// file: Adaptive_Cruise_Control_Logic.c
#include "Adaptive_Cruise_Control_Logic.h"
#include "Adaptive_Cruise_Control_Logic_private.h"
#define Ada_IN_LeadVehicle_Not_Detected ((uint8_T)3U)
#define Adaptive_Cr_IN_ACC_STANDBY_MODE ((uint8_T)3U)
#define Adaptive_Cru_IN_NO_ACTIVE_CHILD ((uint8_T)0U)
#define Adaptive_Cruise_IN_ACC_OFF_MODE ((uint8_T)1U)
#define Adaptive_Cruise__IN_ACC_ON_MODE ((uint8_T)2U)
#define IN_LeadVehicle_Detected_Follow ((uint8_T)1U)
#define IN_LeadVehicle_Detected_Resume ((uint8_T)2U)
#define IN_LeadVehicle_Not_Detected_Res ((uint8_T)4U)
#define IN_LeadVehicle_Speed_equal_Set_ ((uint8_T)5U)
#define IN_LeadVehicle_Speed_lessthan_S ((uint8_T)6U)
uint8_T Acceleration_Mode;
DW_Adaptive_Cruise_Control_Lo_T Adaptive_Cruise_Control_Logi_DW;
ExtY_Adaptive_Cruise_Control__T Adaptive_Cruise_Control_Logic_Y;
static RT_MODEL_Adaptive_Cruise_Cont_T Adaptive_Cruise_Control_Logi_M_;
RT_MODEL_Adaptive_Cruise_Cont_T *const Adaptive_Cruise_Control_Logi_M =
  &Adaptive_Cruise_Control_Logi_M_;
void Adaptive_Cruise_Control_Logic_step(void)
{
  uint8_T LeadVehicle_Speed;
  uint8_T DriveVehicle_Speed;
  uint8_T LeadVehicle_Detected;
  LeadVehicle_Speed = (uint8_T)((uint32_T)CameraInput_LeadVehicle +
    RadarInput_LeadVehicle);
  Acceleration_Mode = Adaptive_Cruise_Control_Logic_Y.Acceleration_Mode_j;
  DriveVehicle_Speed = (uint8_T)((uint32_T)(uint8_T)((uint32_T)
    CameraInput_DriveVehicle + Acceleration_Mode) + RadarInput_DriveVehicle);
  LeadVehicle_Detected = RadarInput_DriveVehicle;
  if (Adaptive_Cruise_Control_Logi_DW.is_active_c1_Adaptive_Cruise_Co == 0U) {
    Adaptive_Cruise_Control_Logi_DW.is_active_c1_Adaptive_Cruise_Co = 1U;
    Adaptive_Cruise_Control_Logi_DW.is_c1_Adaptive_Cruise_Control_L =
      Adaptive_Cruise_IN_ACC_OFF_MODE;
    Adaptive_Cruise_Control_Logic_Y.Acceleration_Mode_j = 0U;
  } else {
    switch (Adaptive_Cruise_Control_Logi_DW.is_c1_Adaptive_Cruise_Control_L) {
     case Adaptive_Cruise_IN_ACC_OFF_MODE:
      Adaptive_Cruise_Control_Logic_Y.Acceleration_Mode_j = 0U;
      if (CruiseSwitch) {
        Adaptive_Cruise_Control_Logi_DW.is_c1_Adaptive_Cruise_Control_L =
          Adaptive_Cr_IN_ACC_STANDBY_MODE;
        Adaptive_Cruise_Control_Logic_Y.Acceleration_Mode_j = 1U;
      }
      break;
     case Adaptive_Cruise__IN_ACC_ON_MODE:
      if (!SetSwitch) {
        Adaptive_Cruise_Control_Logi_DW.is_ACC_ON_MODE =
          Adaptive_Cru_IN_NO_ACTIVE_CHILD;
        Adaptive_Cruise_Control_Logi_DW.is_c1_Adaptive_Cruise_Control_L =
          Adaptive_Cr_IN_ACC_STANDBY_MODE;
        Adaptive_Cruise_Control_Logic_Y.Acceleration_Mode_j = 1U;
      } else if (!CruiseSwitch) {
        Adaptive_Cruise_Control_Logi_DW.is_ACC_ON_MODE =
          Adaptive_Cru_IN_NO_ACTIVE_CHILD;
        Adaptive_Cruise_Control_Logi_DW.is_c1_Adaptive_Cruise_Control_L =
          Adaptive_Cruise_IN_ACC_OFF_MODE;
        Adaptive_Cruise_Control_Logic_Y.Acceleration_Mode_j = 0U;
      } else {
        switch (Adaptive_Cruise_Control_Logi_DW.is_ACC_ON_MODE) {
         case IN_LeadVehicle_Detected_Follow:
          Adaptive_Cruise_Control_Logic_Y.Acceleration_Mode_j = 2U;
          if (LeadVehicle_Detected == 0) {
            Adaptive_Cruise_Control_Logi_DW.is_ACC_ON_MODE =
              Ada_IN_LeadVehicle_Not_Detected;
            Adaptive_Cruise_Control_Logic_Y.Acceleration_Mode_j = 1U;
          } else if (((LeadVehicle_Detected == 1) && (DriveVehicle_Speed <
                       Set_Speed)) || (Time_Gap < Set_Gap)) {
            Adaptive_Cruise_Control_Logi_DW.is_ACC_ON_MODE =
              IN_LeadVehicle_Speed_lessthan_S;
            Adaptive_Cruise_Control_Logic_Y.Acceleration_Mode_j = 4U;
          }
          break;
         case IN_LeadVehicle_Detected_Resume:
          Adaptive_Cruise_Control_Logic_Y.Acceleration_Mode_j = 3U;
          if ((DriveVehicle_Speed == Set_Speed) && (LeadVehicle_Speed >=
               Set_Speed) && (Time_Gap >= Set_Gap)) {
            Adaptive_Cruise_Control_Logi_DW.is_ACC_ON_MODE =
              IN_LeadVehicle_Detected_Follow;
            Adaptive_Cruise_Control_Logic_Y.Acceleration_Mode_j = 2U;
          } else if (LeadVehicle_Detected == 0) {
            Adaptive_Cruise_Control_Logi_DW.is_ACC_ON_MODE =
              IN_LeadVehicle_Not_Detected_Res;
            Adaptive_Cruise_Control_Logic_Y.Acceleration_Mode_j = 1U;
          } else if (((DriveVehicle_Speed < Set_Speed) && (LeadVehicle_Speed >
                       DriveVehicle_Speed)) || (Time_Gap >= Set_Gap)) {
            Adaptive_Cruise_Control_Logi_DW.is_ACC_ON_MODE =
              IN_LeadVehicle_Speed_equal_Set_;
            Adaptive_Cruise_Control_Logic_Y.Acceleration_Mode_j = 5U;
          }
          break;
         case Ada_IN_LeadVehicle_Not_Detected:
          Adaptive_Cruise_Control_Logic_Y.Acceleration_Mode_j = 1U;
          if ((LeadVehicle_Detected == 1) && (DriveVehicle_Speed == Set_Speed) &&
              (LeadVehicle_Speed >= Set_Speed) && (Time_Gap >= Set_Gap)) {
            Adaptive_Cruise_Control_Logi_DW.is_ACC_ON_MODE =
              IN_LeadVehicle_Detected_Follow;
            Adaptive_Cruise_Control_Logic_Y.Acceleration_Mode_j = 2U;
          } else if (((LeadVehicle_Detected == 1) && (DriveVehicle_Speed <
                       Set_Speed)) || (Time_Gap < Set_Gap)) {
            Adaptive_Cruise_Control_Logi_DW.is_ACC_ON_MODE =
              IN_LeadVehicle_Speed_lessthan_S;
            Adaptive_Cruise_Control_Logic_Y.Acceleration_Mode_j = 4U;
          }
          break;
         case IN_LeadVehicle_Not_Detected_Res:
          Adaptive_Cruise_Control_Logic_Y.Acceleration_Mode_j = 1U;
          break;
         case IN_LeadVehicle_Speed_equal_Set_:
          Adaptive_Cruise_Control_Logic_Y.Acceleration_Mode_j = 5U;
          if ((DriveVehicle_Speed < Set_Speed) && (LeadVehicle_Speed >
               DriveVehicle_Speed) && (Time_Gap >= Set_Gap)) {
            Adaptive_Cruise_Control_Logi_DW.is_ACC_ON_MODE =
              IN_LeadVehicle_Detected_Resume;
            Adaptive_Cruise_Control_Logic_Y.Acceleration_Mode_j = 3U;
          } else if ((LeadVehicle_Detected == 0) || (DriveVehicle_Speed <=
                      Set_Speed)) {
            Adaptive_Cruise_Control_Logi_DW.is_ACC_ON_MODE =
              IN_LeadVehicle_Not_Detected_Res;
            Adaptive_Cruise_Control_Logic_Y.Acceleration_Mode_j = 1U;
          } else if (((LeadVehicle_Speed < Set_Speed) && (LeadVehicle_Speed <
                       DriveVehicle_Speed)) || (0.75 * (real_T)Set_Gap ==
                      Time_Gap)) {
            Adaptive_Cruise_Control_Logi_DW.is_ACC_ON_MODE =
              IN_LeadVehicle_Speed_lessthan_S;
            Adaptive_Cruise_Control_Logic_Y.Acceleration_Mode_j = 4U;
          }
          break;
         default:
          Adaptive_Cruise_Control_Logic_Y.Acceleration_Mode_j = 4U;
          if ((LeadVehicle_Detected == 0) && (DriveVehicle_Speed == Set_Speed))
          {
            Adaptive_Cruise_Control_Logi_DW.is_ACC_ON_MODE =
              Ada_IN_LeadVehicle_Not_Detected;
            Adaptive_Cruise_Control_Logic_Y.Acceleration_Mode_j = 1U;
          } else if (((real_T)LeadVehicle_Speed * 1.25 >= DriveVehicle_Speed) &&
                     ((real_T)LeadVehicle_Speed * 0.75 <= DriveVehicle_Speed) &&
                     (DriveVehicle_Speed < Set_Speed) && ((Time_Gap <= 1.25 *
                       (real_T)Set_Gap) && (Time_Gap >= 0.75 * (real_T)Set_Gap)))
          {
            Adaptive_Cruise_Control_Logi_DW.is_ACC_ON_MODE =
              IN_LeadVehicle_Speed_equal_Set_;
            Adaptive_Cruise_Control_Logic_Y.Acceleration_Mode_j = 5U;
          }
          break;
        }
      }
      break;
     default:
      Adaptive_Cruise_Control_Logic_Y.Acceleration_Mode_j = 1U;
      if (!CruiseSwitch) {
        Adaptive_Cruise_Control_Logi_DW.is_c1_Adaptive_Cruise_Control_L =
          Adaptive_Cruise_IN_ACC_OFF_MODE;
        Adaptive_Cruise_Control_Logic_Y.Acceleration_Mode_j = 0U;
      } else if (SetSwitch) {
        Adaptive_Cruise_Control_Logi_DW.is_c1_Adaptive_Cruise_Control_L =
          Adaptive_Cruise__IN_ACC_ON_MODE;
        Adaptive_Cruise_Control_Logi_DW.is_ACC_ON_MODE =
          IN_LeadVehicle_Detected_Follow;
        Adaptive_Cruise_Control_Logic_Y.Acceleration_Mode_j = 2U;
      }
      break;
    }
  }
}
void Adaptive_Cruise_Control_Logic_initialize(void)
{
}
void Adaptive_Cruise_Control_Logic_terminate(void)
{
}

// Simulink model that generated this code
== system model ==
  CameraInput_LeadVehicle : Inport
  RadarInput_LeadVehicle : Inport
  CameraInput_DriveVehicle : Inport
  RadarInput_DriveVehicle : Inport
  CruiseSwitch : Inport
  Time_Gap : Inport
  Set_Speed : Inport
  Set_Gap : Inport
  SetSwitch : Inport
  Acceleration_Mode : Outport  <- 1: Subsystem#1
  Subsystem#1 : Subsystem  <- 1: CameraInput_LeadVehicle, 2: RadarInput_LeadVehicle, 3: CameraInput_DriveVehicle, 4: RadarInput_DriveVehicle, 5: CruiseSwitch, 6: Time_Gap, 7: Set_Speed, 8: Set_Gap, 9: SetSwitch
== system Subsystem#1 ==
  Inport#1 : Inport
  Inport#2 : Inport
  Inport#3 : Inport
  Inport#4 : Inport
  Inport#5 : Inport
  Inport#6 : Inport
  Inport#7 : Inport
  Inport#8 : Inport
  Inport#9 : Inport
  Outport#1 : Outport  <- 1: Stateflowchart#1
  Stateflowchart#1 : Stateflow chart  <- 1: Inport#5, 2: Inport#6, 3: Inport#7, 4: Inport#8, 5: Inport#9, 6: Sum#1, 7: Sum#2, 8: SignalConversion#1
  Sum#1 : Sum  <- 1: Inport#1, 2: Inport#2
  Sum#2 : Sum  Inputs=+++  <- 1: Inport#3, 2: UnitDelay#1, 3: Inport#4
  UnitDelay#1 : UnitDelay  <- 1: Stateflowchart#1
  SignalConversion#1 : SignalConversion  <- 1: Inport#4
== stateflow chart Stateflowchart#1 ==
  state ACC_STANDBY_MODE
    entry:
    Acceleration_Mode=1;
  state ACC_OFF_MODE
    entry:
    Acceleration_Mode = 0;
  state ACC_ON_MODE
    state LeadVehicle_Detected_Resume
      entry:
      Acceleration_Mode=3;
    state LeadVehicle_Not_Detected_Resume
      entry:
      Acceleration_Mode=1;
    state LeadVehicle_Detected_Follow
      entry:
      Acceleration_Mode=2;
    state LeadVehicle_Not_Detected
      entry:
      Acceleration_Mode=1;
    state LeadVehicle_Speed_lessthan_Set_Speed
      entry:
      Acceleration_Mode=4;
    state LeadVehicle_Speed_equal_Set_Speed
      entry:
      Acceleration_Mode=5;
    (default) -> LeadVehicle_Detected_Follow
    LeadVehicle_Detected_Resume -> LeadVehicle_Detected_Follow [order 1] : [(DriveVehicle_Speed == Set_Speed) &&...
        |  (LeadVehicle_Speed >= Set_Speed) &&...
        |  (Time_Gap >= Set_Gap)]
    LeadVehicle_Detected_Resume -> LeadVehicle_Not_Detected_Resume [order 2] : [LeadVehicle_Detected==0]
    LeadVehicle_Detected_Follow -> LeadVehicle_Not_Detected [order 1] : [LeadVehicle_Detected == 0]
    LeadVehicle_Not_Detected -> LeadVehicle_Detected_Follow [order 1] : [(LeadVehicle_Detected == 1)&&...
        | (DriveVehicle_Speed == Set_Speed) &&...
        | (LeadVehicle_Speed >= Set_Speed) &&...
        | (Time_Gap >= Set_Gap)]
    LeadVehicle_Speed_equal_Set_Speed -> LeadVehicle_Detected_Resume [order 1] : [(DriveVehicle_Speed < Set_Speed) &&...
        |  (LeadVehicle_Speed > DriveVehicle_Speed) &&...
        |  (Time_Gap >= Set_Gap)]
    LeadVehicle_Detected_Resume -> LeadVehicle_Speed_equal_Set_Speed [order 3] : [(DriveVehicle_Speed < Set_Speed) &&...
        |  (LeadVehicle_Speed > DriveVehicle_Speed) ||...
        |  (Time_Gap >= Set_Gap)]
    LeadVehicle_Speed_equal_Set_Speed -> LeadVehicle_Not_Detected_Resume [order 2] : [(LeadVehicle_Detected == 0) ||...
        | (DriveVehicle_Speed <= Set_Speed)]
    LeadVehicle_Detected_Follow -> LeadVehicle_Speed_lessthan_Set_Speed [order 2] : [(LeadVehicle_Detected == 1)&&...
        | (DriveVehicle_Speed < Set_Speed) ||...
        | (Time_Gap < Set_Gap)]
    LeadVehicle_Not_Detected -> LeadVehicle_Speed_lessthan_Set_Speed [order 2] : [(LeadVehicle_Detected == 1) &&...
        | (DriveVehicle_Speed < Set_Speed) ||...
        | (Time_Gap < Set_Gap)]
    LeadVehicle_Speed_lessthan_Set_Speed -> LeadVehicle_Not_Detected [order 1] : [(LeadVehicle_Detected == 0) &&...
        | (DriveVehicle_Speed == Set_Speed)]
    LeadVehicle_Speed_equal_Set_Speed -> LeadVehicle_Speed_lessthan_Set_Speed [order 3] : [(LeadVehicle_Speed < Set_Speed) &&...
        | (LeadVehicle_Speed < DriveVehicle_Speed) ||...
        | (Time_Gap ==0.75*Set_Gap)]
    LeadVehicle_Speed_lessthan_Set_Speed -> LeadVehicle_Speed_equal_Set_Speed [order 2] : [((LeadVehicle_Speed*1.25>=DriveVehicle_Speed) &&...
        | (LeadVehicle_Speed * 0.75<=DriveVehicle_Speed)) &&...
        | (DriveVehicle_Speed < Set_Speed) &&...
        | ((Time_Gap<=1.25*Set_Gap) &&...
        | (Time_Gap >=0.75*Set_Gap))]
  (default) -> ACC_OFF_MODE
  ACC_OFF_MODE -> ACC_STANDBY_MODE : [CruiseSwitch==1]
  ACC_STANDBY_MODE -> ACC_OFF_MODE [order 1] : [CruiseSwitch==0]
  ACC_ON_MODE -> ACC_OFF_MODE [order 2] : [CruiseSwitch==0]
  ACC_STANDBY_MODE -> ACC_ON_MODE [order 2] : [SetSwitch==1]
  ACC_ON_MODE -> ACC_STANDBY_MODE [order 1] : [SetSwitch==0]
  data: CruiseSwitch input size=1; Time_Gap input size=1; Set_Speed input size=1; Set_Gap input size=1; SetSwitch input size=1; LeadVehicle_Speed input size=1; DriveVehicle_Speed input size=1; LeadVehicle_Detected input size=1; Acceleration_Mode output uint8 size=1
